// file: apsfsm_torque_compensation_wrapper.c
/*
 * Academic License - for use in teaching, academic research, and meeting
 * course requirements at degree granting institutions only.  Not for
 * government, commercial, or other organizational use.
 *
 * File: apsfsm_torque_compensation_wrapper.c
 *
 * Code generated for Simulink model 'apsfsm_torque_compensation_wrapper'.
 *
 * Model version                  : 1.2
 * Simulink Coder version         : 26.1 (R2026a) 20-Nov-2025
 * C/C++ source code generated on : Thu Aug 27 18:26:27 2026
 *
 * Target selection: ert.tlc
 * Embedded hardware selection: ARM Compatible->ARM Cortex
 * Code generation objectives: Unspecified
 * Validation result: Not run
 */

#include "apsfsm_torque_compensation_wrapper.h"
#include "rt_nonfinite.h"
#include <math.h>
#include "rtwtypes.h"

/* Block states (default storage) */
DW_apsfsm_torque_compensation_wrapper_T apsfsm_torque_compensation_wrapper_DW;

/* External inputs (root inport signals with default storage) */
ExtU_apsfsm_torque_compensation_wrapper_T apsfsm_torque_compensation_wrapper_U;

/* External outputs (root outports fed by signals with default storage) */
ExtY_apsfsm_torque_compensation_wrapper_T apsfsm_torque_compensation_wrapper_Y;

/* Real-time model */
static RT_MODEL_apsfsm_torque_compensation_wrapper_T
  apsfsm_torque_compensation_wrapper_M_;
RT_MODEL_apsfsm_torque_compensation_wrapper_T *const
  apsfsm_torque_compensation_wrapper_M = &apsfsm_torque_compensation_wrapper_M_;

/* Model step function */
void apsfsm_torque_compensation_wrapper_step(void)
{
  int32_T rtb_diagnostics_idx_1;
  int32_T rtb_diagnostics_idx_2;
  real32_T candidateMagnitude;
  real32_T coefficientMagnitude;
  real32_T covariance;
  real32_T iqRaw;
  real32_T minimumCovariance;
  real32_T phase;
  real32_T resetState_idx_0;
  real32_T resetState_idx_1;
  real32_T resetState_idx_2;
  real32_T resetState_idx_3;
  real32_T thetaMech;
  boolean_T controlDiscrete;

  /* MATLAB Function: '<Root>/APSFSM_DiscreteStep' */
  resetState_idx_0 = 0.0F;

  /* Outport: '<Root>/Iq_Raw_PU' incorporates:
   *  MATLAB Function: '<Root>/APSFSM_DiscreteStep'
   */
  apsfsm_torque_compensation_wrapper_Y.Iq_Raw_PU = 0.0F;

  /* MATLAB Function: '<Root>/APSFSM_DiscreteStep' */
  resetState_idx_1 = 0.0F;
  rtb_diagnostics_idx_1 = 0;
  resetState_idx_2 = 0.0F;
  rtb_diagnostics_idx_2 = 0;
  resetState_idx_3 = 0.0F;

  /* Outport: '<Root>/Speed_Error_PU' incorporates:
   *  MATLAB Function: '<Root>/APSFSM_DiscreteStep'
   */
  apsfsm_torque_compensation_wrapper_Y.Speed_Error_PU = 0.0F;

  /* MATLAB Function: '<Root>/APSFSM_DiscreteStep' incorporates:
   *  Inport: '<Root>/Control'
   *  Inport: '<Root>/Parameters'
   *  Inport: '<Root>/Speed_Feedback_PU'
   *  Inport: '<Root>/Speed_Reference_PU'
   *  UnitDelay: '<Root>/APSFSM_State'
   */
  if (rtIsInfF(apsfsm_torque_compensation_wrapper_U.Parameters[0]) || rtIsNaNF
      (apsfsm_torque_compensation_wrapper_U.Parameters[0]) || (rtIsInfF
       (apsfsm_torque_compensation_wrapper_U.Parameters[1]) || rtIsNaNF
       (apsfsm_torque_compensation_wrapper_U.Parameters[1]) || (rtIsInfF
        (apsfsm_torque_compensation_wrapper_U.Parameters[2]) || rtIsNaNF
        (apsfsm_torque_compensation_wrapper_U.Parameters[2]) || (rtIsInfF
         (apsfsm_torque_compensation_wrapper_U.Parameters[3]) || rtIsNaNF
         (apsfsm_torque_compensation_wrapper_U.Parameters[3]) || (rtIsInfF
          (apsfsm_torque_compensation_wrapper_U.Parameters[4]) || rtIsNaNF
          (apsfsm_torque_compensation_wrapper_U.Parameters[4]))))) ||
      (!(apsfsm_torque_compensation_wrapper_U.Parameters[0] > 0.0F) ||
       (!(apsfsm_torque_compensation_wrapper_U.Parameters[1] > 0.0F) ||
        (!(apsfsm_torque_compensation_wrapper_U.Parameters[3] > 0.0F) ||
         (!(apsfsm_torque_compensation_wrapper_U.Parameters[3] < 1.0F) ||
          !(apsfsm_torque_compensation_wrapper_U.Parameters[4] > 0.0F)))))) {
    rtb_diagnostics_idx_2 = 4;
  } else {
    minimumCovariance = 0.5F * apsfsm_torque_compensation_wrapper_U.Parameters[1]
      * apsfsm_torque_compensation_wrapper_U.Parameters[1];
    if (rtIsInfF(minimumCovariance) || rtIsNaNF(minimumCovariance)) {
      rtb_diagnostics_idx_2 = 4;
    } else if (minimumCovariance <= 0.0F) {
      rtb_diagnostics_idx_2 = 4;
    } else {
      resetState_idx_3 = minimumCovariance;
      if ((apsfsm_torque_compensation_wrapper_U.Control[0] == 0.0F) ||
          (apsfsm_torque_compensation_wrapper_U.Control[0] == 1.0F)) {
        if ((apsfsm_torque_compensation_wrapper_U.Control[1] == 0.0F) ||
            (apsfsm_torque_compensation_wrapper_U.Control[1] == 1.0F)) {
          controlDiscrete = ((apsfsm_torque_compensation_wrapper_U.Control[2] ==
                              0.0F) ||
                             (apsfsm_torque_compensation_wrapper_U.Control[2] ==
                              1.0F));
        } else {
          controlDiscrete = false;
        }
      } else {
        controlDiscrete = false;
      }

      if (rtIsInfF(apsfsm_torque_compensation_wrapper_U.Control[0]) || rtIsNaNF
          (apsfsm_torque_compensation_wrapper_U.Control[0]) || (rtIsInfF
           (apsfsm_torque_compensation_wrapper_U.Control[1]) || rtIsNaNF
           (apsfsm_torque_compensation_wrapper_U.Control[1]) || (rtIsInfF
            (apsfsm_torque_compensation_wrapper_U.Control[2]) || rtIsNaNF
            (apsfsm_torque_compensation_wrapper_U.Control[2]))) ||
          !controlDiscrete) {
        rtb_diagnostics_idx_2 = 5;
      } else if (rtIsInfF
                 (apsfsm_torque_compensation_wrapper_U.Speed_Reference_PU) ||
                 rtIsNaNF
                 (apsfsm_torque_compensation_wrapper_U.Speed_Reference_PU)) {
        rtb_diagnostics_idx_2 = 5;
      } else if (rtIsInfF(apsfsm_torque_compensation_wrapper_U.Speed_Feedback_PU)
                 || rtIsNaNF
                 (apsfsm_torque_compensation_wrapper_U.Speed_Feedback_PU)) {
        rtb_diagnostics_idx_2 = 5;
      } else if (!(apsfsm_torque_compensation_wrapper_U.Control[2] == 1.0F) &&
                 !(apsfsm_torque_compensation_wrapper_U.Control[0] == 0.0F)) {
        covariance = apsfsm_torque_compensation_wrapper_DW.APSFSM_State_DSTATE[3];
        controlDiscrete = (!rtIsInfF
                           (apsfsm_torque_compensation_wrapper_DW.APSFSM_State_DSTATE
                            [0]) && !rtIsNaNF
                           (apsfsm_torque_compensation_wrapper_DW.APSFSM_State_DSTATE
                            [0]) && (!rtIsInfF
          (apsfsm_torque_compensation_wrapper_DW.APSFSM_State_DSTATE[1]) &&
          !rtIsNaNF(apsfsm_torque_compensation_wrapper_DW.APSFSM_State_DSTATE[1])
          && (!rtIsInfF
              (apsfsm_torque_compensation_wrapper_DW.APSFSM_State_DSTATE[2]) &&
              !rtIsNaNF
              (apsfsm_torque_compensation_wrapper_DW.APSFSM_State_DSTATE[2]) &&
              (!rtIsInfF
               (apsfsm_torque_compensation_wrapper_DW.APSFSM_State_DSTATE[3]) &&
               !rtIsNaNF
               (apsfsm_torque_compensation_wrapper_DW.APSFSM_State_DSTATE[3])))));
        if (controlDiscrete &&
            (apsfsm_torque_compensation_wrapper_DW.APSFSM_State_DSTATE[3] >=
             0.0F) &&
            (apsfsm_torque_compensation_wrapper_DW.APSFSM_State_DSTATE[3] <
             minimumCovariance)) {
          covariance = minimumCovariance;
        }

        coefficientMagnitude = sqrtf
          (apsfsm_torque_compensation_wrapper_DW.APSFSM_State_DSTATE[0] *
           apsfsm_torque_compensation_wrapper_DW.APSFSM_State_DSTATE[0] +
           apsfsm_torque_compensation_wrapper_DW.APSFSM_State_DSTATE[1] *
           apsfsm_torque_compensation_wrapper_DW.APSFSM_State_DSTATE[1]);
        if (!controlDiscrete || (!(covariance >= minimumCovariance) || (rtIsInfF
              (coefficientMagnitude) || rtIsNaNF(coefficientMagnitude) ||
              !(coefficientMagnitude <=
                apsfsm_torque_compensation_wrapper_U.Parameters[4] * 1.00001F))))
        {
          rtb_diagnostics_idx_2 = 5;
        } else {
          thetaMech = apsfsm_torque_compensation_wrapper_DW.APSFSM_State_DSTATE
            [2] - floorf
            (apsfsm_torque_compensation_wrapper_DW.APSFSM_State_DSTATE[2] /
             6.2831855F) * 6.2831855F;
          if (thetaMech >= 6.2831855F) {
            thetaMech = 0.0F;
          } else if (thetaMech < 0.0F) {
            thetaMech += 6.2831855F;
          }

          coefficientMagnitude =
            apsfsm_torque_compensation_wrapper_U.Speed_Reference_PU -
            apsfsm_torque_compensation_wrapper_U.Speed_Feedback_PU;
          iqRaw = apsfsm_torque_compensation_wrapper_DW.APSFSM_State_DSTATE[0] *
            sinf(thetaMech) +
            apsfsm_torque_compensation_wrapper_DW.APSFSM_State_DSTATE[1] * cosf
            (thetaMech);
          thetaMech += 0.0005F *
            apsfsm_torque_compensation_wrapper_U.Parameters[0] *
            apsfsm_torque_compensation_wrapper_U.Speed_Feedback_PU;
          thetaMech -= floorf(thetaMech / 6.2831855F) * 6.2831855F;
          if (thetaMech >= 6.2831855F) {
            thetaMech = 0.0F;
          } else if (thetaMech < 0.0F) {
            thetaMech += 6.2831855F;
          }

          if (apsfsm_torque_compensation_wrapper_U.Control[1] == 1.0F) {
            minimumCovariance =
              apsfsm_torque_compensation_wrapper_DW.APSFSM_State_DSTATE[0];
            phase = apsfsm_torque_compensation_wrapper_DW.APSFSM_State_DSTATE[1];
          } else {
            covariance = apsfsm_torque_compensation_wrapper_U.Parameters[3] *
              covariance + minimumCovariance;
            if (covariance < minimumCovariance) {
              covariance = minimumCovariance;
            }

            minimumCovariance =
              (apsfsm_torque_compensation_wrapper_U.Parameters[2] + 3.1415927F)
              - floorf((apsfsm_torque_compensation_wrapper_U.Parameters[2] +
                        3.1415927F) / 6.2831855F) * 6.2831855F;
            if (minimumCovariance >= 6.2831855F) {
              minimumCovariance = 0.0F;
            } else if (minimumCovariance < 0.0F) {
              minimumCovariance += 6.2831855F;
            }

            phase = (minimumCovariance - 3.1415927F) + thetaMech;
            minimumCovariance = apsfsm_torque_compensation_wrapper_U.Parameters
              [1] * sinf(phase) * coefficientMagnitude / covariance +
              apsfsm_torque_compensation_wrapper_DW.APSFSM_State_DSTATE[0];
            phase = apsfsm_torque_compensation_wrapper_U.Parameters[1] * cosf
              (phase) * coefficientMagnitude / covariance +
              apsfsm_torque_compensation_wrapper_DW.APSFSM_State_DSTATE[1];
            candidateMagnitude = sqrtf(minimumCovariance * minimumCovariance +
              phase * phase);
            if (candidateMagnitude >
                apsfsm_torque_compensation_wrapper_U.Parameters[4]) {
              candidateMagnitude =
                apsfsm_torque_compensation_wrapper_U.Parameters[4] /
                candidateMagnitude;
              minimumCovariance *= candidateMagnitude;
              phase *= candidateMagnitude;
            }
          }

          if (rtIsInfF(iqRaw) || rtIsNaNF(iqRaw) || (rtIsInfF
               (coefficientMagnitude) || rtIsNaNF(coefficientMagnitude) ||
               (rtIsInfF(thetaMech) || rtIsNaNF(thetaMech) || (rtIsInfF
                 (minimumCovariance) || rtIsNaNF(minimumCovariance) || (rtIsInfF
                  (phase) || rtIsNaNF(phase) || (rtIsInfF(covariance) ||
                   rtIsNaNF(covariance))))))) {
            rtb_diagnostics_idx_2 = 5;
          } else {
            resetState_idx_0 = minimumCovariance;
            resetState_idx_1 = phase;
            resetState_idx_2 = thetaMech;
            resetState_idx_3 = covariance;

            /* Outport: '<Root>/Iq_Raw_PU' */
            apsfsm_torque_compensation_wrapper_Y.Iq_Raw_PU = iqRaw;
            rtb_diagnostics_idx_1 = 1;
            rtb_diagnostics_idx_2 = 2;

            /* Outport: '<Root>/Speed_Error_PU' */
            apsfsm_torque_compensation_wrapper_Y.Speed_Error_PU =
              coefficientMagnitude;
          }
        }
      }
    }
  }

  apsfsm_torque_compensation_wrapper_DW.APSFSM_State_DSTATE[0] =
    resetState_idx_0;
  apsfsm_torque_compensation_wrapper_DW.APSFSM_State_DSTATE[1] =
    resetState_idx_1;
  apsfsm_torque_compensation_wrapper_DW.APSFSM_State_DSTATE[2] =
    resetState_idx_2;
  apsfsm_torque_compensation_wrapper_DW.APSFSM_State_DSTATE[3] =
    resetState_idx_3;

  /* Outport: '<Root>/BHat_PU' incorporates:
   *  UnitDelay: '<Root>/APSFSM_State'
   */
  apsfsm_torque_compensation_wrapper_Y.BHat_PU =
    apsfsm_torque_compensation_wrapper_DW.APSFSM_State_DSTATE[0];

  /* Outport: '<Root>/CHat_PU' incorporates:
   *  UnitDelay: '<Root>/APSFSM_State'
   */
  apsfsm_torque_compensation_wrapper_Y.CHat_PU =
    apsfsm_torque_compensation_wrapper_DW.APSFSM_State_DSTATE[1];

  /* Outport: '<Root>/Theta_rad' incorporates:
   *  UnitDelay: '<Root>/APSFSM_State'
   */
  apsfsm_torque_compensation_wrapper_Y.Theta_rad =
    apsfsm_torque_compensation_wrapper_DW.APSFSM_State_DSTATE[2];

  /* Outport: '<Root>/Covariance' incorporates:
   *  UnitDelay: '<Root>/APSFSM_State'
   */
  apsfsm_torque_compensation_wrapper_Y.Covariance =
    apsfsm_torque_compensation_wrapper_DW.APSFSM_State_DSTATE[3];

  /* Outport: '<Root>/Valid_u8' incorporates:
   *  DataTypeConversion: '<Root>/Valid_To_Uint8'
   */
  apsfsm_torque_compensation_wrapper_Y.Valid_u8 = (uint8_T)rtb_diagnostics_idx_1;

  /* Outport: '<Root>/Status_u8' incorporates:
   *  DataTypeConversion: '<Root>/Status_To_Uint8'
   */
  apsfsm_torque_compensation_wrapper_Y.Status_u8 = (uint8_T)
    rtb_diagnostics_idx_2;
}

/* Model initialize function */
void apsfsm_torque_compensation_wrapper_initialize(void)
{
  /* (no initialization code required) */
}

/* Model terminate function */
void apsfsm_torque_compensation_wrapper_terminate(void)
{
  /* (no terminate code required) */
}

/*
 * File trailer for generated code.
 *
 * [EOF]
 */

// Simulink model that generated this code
simulink model "apsfsm_torque_compensation_wrapper"  (R2026a)
settings: Solver=FixedStepDiscrete  StopTime=0.01  FixedStep=5e-4

== system apsfsm_torque_compensation_wrapper ==
  Speed_Reference_PU : Inport  OutDataTypeStr=single  PortDimensions=1
  Speed_Feedback_PU : Inport  Port=2  OutDataTypeStr=single  PortDimensions=1
  Parameters : Inport  Port=3  OutDataTypeStr=single  PortDimensions=5
  Control : Inport  Port=4  OutDataTypeStr=single  PortDimensions=3
  APSFSM_DiscreteStep : MATLAB Function  TreatAsAtomicUnit=on
  APSFSM_State : UnitDelay  InitialCondition=single([0;0;0;0])  SampleTime=-1
  Diagnostic_Demux : Demux
  State_Demux : Demux
  Status_To_Uint8 : DataTypeConversion  OutDataTypeStr=uint8
  Valid_To_Uint8 : DataTypeConversion  OutDataTypeStr=uint8
  Iq_Raw_PU : Outport  OutDataTypeStr=single
  Valid_u8 : Outport  Port=2  OutDataTypeStr=uint8
  Status_u8 : Outport  Port=3  OutDataTypeStr=uint8
  BHat_PU : Outport  Port=4  OutDataTypeStr=single
  CHat_PU : Outport  Port=5  OutDataTypeStr=single
  Theta_rad : Outport  Port=6  OutDataTypeStr=single
  Speed_Error_PU : Outport  Port=7  OutDataTypeStr=single
  Covariance : Outport  Port=8  OutDataTypeStr=single
  wires:
  APSFSM_State/1 -> APSFSM_DiscreteStep/1(state)
  Speed_Reference_PU/1 -> APSFSM_DiscreteStep/2(speedReferencePU)
  Speed_Feedback_PU/1 -> APSFSM_DiscreteStep/3(speedFeedbackPU)
  Parameters/1 -> APSFSM_DiscreteStep/4(parameters)
  Control/1 -> APSFSM_DiscreteStep/5(control)
  APSFSM_DiscreteStep/1(stateNext) -> State_Demux/1, APSFSM_State/1
  APSFSM_DiscreteStep/2(diagnostics) -> Diagnostic_Demux/1
  Diagnostic_Demux/1 -> Iq_Raw_PU/1
  Diagnostic_Demux/2 -> Valid_To_Uint8/1
  Valid_To_Uint8/1 -> Valid_u8/1
  Diagnostic_Demux/3 -> Status_To_Uint8/1
  Status_To_Uint8/1 -> Status_u8/1
  State_Demux/1 -> BHat_PU/1
  State_Demux/2 -> CHat_PU/1
  State_Demux/3 -> Theta_rad/1
  Diagnostic_Demux/4 -> Speed_Error_PU/1
  State_Demux/4 -> Covariance/1

== matlab function apsfsm_torque_compensation_wrapper/APSFSM_DiscreteStep ==
function [stateNext, diagnostics] = APSFSM_DiscreteStep(state, speedReferencePU, speedFeedbackPU, parameters, control)
%#codegen
[stateNext, diagnostics] = apsfsmTorqueCompensationStep(state, speedReferencePU, speedFeedbackPU, parameters, control);
end
